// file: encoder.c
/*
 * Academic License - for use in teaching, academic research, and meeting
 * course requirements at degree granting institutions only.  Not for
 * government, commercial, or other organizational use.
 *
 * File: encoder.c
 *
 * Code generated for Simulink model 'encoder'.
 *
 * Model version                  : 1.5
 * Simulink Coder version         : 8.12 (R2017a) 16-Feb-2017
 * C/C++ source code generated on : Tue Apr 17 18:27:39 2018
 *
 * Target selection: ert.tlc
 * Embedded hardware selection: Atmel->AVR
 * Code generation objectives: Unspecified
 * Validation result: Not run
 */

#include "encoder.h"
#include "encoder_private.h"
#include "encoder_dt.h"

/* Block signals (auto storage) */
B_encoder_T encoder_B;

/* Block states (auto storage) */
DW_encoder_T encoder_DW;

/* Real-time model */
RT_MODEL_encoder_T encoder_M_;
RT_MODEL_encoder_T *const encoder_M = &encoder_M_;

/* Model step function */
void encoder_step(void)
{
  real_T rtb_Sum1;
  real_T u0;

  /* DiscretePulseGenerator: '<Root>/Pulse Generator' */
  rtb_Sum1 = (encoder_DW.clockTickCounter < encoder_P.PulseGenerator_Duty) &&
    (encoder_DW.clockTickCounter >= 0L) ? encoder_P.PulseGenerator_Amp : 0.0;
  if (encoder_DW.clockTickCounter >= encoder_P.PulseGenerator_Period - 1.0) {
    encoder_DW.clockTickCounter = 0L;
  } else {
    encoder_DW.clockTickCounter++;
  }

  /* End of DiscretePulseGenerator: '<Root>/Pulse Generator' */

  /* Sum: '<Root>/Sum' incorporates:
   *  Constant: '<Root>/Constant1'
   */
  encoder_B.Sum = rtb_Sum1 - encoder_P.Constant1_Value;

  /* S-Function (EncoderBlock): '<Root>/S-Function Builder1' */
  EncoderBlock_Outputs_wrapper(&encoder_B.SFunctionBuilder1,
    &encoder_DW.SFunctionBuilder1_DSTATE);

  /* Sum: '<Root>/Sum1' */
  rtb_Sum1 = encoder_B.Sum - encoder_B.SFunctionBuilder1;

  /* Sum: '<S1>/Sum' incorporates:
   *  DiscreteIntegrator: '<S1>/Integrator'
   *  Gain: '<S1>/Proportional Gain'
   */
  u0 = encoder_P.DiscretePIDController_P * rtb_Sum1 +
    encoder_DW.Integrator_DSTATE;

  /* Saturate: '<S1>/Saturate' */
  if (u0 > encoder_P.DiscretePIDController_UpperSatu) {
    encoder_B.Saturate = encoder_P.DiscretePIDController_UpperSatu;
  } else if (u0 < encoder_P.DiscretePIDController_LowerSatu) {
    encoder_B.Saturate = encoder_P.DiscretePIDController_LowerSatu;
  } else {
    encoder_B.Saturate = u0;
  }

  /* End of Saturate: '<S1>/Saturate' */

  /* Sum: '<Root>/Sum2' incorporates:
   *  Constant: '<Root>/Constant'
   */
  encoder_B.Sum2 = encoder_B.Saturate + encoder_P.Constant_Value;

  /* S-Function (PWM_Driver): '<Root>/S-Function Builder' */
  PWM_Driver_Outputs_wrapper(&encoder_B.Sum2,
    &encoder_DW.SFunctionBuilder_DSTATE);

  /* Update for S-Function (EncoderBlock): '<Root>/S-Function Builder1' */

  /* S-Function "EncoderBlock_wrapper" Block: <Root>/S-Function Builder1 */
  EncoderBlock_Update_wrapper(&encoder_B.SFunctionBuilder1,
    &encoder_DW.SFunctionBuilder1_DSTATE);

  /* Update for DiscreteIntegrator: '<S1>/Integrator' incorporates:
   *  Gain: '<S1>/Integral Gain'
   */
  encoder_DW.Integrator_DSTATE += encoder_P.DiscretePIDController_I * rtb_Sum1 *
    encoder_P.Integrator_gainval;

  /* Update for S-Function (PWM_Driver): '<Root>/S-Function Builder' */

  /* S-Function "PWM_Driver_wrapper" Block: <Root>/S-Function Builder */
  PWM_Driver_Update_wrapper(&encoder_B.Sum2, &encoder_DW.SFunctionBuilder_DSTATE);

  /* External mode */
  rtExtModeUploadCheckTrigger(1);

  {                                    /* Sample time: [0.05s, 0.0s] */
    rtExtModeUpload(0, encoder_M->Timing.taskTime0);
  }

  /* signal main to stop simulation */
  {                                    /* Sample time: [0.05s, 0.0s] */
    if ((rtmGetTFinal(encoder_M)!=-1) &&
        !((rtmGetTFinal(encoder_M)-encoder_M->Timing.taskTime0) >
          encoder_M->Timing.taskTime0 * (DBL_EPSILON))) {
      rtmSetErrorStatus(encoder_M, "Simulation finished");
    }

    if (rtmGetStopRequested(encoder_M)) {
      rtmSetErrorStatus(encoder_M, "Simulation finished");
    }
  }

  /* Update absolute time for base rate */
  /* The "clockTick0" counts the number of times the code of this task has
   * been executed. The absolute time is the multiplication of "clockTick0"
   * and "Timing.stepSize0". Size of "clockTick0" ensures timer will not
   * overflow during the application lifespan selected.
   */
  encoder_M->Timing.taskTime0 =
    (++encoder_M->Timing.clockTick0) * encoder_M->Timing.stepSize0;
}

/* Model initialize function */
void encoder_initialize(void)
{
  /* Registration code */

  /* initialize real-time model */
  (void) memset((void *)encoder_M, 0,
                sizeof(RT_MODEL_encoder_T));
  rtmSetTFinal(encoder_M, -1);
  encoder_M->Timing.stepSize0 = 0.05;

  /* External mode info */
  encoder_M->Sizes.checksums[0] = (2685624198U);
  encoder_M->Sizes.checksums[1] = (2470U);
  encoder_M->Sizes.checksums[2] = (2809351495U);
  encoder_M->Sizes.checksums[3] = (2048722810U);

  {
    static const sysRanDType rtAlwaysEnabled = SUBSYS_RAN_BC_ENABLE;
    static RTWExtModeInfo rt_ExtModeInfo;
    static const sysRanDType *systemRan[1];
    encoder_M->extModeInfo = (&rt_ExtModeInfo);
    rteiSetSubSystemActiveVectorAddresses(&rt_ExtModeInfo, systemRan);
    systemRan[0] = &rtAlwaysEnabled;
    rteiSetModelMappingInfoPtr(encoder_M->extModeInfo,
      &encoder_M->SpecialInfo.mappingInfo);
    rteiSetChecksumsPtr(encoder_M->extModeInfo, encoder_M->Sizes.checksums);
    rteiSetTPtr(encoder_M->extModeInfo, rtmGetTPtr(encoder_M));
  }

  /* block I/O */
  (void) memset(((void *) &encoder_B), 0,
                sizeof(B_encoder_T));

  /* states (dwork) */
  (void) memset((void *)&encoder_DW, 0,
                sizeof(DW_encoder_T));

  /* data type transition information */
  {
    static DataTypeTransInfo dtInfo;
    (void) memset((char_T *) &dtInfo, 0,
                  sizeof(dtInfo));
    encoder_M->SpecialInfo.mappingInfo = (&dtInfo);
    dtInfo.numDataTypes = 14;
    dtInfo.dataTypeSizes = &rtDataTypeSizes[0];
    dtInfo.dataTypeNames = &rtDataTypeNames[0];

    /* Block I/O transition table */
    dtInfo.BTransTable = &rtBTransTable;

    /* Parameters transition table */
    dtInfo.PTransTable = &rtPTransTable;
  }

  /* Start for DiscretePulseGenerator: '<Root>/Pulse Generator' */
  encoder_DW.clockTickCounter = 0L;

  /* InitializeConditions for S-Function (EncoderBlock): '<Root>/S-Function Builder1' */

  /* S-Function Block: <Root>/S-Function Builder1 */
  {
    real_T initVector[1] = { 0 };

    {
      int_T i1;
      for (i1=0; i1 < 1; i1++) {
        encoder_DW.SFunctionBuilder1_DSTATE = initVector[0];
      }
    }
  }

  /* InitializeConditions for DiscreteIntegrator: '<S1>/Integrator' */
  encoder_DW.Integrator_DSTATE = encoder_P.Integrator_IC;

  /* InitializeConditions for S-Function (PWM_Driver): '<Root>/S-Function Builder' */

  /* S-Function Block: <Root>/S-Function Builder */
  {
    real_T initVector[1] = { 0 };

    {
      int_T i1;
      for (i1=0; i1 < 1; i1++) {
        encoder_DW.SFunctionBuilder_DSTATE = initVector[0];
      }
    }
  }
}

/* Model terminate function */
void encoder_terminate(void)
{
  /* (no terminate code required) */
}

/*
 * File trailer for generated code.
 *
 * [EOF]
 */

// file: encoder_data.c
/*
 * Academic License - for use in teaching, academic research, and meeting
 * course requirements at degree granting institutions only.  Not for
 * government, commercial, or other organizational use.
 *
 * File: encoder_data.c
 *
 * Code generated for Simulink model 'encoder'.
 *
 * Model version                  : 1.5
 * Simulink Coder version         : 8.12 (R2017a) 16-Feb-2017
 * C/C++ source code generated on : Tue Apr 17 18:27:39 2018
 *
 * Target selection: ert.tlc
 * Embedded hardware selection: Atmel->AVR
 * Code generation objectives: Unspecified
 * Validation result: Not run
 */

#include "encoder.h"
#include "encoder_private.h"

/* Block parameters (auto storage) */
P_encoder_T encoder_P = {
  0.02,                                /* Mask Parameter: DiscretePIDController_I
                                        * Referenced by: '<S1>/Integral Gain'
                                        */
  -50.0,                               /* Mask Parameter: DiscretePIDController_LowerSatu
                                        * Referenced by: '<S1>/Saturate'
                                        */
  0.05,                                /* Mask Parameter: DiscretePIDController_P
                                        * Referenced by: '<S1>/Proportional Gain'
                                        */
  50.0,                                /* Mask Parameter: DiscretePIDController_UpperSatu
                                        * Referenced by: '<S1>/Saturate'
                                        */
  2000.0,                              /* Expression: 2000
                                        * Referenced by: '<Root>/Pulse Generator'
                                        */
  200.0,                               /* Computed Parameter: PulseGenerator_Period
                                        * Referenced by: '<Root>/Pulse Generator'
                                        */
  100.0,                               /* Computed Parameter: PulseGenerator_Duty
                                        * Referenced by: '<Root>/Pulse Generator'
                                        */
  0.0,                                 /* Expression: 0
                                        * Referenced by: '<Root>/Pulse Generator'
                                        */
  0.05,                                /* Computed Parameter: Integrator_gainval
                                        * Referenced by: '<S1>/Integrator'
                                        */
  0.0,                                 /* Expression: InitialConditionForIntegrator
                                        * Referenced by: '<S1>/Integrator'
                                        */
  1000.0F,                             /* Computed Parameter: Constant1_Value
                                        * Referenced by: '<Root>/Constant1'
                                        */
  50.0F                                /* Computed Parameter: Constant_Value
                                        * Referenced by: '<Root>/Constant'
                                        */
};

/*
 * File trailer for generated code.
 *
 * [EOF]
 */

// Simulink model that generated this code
simulink model "encoder"  (R2017a)
settings: Solver=FixedStepAuto  StartTime=0.0  StopTime=inf  FixedStep=0.05  RelTol=1e-3  EnableMultiTasking=on
libraries: simulink x1

== system encoder ==
  Constant : Constant  Value=50  OutDataTypeStr=single
  Constant1 : Constant  Value=1000  OutDataTypeStr=single
  Discrete PID Controller : simulink/Continuous/PID Controller  Controller=PI  TimeDomain=Discrete-time  SampleTime=-1  IntegratorMethod=Forward Euler  FilterMethod=Forward Euler  Form=Parallel  UseFilter=on  ControllerParametersSource=internal  P=0.2  I=0.12  D=0  N=100  InitialConditionSource=internal  InitialConditionForIntegrator=0  InitialConditionForFilter=0  ExternalReset=none  LimitOutput=on  UpperSaturationLimit=50  LowerSaturationLimit=-50  LinearizeAsGain=off  AntiWindupMode=none  Kb=1  TrackingMode=off  Kt=1  PParamMin=[]  PParamMax=[]  IParamMin=[]  IParamMax=[]  DParamMin=[]  DParamMax=[]  NParamMin=[]  NParamMax=[]  KbParamMin=[]  KbParamMax=[]  KtParamMin=[]  KtParamMax=[]  POutMin=[]  POutMax=[]  IOutMin=[]  IOutMax=[]  DOutMin=[]  DOutMax=[]  NOutMin=[]  NOutMax=[]  KbOutMin=[]  KbOutMax=[]  KtOutMin=[]  KtOutMax=[]  IntegratorOutMin=[]  IntegratorOutMax=[]  FilterOutMin=[]  FilterOutMax=[]  SumOutMin=[]  SumOutMax=[]  SumI1OutMin=[]  SumI1OutMax=[]  SumI2OutMin=[]  SumI2OutMax=[]  SumI3OutMin=[]  SumI3OutMax=[]  SumDOutMin=[]  SumDOutMax=[]  SaturationOutMin=[]  SaturationOutMax=[]  IntegratorContinuousStateAttributes=''  IntegratorStateMustResolveToSignalObject=off  IntegratorRTWStateStorageClass=Auto  FilterContinuousStateAttributes=''  FilterStateMustResolveToSignalObject=off  FilterRTWStateStorageClass=Auto  DifferentiatorICPrevScaledInput=0  DifferentiatorOutMin=[]  DifferentiatorOutMax=[]  InitialConditionSetting=State (most efficient)
  Mux : Mux  Inputs=2
  Pulse Generator : DiscretePulseGenerator  PulseType=Time based  Amplitude=2000  Period=10  PulseWidth=50
  S-Function Builder : S-Function  InitFcn=try, set_param(gcb,'FunctionName','PWM_Driver'), end  FunctionName=PWM_Driver  SFunctionModules=PWM_Driver_wrapper  SFunctionDeploymentMode=off  EnableBusSupport=off  mask(S-Function Builder){}
      mask help: Simulink:masks:SFunctionBuilder_MD
      mask init:
      | val = [[.9  0.75 0.75 1 1 .9 .9 1]',[1 1 0.75 0.75 .9 .9 1 .9]'];try , sys = get_param(gcb,'SfunBuilderFcnName');if isempty(sys), sys = get_param(gcb,'FunctionName'); end,catch, sys = get_param(gcb,'FunctionName'); end
  S-Function Builder1 : S-Function  InitFcn=try, set_param(gcb,'FunctionName','EncoderBlock'), end  FunctionName=EncoderBlock  SFunctionModules=EncoderBlock_wrapper  SFunctionDeploymentMode=off  EnableBusSupport=off  mask(S-Function Builder){}
      mask help: Simulink:masks:SFunctionBuilder_MD
      mask init: same as encoder/S-Function Builder
  Scope : Scope
  Scope1 : Scope
  Sum : Sum  Inputs=|+-
  Sum1 : Sum  Inputs=+-
  Sum2 : Sum  Inputs=|++
  wires:
  Pulse Generator/1 -> Sum/1
  Constant1/1 -> Sum/2
  S-Function Builder1/1 -> Mux/1, Sum1/2
  Sum/1 -> Mux/2, Sum1/1
  Mux/1 -> Scope1/1
  Constant/1 -> Sum2/2
  Sum2/1 -> S-Function Builder/1
  Discrete PID Controller/1 -> Scope/1, Sum2/1
  Sum1/1 -> Discrete PID Controller/1
